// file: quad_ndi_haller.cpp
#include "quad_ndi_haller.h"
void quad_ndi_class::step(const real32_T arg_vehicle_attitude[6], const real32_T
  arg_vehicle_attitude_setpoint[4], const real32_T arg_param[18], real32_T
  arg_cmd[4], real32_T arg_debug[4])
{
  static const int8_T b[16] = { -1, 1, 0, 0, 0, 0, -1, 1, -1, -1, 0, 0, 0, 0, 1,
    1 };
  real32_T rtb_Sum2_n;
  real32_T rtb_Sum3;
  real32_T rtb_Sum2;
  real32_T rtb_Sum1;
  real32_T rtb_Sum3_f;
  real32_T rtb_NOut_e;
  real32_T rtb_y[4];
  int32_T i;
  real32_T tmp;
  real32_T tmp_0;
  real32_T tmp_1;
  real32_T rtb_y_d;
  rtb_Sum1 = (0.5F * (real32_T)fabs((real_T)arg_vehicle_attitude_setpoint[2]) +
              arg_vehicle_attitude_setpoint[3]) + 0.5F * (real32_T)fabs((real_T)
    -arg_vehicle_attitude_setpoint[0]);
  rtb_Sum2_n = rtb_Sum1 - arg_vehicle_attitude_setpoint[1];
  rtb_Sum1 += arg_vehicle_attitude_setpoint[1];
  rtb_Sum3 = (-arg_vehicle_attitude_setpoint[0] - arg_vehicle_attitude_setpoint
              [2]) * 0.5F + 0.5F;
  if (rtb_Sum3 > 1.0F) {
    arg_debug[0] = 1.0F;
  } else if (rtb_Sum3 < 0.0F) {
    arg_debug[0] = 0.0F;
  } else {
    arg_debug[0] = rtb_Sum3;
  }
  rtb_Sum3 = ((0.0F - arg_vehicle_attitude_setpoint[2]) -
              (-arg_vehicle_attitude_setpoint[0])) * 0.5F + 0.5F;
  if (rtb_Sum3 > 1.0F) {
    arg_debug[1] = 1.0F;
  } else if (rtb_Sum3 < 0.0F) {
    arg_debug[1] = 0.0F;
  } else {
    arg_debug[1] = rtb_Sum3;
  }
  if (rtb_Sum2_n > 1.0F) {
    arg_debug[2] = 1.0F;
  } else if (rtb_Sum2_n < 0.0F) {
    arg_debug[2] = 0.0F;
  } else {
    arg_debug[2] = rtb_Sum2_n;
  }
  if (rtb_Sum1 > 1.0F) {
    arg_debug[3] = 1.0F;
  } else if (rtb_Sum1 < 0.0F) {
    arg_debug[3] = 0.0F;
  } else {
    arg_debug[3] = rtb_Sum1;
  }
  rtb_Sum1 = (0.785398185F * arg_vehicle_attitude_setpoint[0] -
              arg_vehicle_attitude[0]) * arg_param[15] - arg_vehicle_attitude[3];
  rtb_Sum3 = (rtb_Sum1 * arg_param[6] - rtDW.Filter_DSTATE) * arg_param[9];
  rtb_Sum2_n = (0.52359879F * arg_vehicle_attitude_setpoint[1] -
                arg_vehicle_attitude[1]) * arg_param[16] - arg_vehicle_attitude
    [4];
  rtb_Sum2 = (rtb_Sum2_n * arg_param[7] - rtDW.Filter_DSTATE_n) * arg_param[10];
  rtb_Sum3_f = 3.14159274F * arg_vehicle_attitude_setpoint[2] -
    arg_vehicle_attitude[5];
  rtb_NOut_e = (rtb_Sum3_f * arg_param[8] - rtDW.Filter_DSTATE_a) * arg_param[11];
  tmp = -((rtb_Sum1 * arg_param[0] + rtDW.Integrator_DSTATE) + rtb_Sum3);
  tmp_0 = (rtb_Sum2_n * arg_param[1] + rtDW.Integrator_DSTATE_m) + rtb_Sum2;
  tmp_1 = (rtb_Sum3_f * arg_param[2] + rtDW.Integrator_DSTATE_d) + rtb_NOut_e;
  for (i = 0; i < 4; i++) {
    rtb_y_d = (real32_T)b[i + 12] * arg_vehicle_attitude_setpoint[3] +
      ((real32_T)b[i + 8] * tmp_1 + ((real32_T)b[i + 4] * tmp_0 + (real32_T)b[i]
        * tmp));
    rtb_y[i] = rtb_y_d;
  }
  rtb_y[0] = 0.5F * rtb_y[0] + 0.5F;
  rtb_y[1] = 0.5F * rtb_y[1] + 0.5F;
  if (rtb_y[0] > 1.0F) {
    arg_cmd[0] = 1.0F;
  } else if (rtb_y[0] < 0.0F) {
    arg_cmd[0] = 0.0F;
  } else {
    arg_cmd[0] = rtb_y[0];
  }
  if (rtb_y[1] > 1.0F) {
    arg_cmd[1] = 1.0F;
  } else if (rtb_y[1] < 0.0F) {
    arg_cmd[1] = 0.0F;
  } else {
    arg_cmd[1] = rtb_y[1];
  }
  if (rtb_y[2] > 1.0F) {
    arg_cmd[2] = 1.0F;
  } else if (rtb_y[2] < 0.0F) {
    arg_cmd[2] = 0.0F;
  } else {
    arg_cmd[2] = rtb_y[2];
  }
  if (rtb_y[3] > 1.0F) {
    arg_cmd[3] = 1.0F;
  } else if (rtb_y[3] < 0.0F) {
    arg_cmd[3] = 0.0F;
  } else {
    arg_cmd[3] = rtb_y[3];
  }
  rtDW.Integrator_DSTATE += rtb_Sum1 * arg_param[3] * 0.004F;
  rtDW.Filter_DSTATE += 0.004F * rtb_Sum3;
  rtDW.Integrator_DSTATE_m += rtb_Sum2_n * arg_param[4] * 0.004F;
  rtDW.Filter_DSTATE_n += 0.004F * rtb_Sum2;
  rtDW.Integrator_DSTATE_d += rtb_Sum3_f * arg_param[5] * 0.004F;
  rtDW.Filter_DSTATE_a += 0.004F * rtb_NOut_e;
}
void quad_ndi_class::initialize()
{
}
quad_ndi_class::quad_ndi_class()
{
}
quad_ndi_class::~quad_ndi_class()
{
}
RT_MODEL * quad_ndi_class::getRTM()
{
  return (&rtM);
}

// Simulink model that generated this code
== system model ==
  vehicle_attitude : Inport
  vehicle_attitude_setpoint : Inport
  param : Inport
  debug : Outport  <- 1: Saturate#1
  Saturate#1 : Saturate  UpperLimit=1  LowerLimit=0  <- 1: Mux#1
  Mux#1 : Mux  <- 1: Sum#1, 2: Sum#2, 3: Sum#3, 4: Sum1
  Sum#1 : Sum  Inputs=++  <- 1: Constant#1, 2: Gain#1
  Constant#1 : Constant  Value=0.5
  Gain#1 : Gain  Gain=0.5  <- 1: Sum3
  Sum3 : Sum  Inputs=+-  <- 1: Gain#2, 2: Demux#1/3
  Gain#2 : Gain  Gain=-1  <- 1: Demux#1
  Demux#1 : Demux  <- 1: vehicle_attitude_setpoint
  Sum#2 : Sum  Inputs=++  <- 1: Constant#1, 2: Gain#3
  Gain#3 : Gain  Gain=0.5  <- 1: Sum2
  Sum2 : Sum  Inputs=--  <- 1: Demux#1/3, 2: Gain#2
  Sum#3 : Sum  Inputs=-+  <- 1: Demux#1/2, 2: Sum#4
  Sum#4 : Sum  Inputs=+++  <- 1: Gain#4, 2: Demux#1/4, 3: Gain#5
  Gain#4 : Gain  Gain=0.5  <- 1: Abs#1
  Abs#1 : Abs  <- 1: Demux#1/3
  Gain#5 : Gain  Gain=0.5  <- 1: Abs#2
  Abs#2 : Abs  <- 1: Gain#2
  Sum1 : Sum  Inputs=++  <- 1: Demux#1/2, 2: Sum#4
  cmd : Outport  <- 1: Saturate#2
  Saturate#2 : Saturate  UpperLimit=1  LowerLimit=0  <- 1: MATLABFunction#1
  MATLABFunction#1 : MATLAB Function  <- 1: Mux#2
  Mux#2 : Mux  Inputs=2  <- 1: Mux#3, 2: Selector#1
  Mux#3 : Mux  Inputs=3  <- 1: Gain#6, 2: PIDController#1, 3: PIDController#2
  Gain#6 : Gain  Gain=-1  <- 1: PIDController#3
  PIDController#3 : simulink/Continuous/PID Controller  Controller=PID  TimeDomain=Discrete-time  IntegratorMethod=Forward Euler  Form=Parallel  P=1  I=1  D=1  N=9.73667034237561  InitialConditionForIntegrator=0  ExternalReset=none  LimitOutput=off  UpperSaturationLimit=inf  LowerSaturationLimit=-inf  <- 1: Sum#5, 2: Selector#2, 3: Selector#3, 4: Selector#4, 5: Selector#5
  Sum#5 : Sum  Inputs=+-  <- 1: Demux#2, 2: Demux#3
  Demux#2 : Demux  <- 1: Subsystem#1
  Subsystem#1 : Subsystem  <- 1: Selector#6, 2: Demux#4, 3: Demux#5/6
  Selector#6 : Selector  Indices=1:3  <- 1: vehicle_attitude_setpoint
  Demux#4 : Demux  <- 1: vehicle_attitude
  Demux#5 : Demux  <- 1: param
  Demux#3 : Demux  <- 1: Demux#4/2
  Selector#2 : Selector  Indices=1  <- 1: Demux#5
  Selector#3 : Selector  Indices=1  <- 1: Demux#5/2
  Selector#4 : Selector  Indices=1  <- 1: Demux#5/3
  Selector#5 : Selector  Indices=1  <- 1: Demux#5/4
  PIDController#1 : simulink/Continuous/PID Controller  Controller=PID  TimeDomain=Discrete-time  IntegratorMethod=Forward Euler  Form=Parallel  P=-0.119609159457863  I=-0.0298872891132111  D=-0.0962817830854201  N=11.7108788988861  InitialConditionForIntegrator=0  ExternalReset=none  LimitOutput=off  UpperSaturationLimit=inf  LowerSaturationLimit=-inf  <- 1: Sum#6, 2: Selector#7, 3: Selector#8, 4: Selector#9, 5: Selector#10
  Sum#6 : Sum  Inputs=-+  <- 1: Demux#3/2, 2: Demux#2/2
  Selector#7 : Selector  Indices=2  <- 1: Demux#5
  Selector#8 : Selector  Indices=2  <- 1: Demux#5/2
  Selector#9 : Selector  Indices=2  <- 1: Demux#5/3
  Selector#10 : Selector  Indices=2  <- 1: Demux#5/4
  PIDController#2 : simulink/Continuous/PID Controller  Controller=PID  TimeDomain=Discrete-time  IntegratorMethod=Forward Euler  Form=Parallel  P=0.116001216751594  I=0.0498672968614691  D=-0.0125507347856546  N=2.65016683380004  InitialConditionForIntegrator=0  ExternalReset=none  LimitOutput=off  UpperSaturationLimit=inf  LowerSaturationLimit=-inf  <- 1: Sum#7, 2: Selector#11, 3: Selector#12, 4: Selector#13, 5: Selector#14
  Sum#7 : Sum  Inputs=-+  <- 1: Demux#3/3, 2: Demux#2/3
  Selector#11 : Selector  Indices=3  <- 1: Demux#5
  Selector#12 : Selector  Indices=3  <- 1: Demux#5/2
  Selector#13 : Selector  Indices=3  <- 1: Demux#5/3
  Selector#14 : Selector  Indices=3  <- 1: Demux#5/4
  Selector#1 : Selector  Indices=4  <- 1: vehicle_attitude_setpoint
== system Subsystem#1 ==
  attitude_setpoint : Inport
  Inport#1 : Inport
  Inport#2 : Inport
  Outport#1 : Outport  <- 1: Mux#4
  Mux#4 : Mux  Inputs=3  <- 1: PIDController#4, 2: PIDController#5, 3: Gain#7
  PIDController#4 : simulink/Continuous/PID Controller  Controller=P  TimeDomain=Discrete-time  IntegratorMethod=Forward Euler  Form=Parallel  P=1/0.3  I=0  D=0  N=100  InitialConditionForIntegrator=0  ExternalReset=none  LimitOutput=off  UpperSaturationLimit=inf  LowerSaturationLimit=-inf  <- 1: Sum#8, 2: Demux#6
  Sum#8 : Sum  Inputs=+-  <- 1: Gain#8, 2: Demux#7
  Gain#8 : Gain  Gain=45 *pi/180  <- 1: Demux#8
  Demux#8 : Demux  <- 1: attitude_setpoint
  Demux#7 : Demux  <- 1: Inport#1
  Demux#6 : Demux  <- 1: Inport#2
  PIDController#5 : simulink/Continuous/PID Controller  Controller=P  TimeDomain=Discrete-time  IntegratorMethod=Forward Euler  Form=Parallel  P=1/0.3  I=0  D=0  N=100  InitialConditionForIntegrator=0  ExternalReset=none  LimitOutput=off  UpperSaturationLimit=inf  LowerSaturationLimit=-inf  <- 1: Sum#9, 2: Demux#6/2
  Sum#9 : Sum  Inputs=+-  <- 1: Gain#9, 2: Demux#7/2
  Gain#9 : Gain  Gain=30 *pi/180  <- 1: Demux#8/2
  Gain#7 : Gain  Gain=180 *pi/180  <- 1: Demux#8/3
== matlab function MATLABFunction#1 ==
function y = fcn(u)

% Mixing Matrix
%      R  P  Y  T
M =  [-1  0 -1  0;  % s1
       1  0 -1  0;  % s2
       0 -1  0  1;  % u1
       0  1  0  1]; % u2

% Mixing Matrix mit Steuergrößen multiplizieren   
y = M * u;

% Servo Offset, da Servocommand 0 = 90° entspricht
y(1) = 0.5 + 0.5 * y(1);
y(2) = 0.5 + 0.5 * y(2);

y;
